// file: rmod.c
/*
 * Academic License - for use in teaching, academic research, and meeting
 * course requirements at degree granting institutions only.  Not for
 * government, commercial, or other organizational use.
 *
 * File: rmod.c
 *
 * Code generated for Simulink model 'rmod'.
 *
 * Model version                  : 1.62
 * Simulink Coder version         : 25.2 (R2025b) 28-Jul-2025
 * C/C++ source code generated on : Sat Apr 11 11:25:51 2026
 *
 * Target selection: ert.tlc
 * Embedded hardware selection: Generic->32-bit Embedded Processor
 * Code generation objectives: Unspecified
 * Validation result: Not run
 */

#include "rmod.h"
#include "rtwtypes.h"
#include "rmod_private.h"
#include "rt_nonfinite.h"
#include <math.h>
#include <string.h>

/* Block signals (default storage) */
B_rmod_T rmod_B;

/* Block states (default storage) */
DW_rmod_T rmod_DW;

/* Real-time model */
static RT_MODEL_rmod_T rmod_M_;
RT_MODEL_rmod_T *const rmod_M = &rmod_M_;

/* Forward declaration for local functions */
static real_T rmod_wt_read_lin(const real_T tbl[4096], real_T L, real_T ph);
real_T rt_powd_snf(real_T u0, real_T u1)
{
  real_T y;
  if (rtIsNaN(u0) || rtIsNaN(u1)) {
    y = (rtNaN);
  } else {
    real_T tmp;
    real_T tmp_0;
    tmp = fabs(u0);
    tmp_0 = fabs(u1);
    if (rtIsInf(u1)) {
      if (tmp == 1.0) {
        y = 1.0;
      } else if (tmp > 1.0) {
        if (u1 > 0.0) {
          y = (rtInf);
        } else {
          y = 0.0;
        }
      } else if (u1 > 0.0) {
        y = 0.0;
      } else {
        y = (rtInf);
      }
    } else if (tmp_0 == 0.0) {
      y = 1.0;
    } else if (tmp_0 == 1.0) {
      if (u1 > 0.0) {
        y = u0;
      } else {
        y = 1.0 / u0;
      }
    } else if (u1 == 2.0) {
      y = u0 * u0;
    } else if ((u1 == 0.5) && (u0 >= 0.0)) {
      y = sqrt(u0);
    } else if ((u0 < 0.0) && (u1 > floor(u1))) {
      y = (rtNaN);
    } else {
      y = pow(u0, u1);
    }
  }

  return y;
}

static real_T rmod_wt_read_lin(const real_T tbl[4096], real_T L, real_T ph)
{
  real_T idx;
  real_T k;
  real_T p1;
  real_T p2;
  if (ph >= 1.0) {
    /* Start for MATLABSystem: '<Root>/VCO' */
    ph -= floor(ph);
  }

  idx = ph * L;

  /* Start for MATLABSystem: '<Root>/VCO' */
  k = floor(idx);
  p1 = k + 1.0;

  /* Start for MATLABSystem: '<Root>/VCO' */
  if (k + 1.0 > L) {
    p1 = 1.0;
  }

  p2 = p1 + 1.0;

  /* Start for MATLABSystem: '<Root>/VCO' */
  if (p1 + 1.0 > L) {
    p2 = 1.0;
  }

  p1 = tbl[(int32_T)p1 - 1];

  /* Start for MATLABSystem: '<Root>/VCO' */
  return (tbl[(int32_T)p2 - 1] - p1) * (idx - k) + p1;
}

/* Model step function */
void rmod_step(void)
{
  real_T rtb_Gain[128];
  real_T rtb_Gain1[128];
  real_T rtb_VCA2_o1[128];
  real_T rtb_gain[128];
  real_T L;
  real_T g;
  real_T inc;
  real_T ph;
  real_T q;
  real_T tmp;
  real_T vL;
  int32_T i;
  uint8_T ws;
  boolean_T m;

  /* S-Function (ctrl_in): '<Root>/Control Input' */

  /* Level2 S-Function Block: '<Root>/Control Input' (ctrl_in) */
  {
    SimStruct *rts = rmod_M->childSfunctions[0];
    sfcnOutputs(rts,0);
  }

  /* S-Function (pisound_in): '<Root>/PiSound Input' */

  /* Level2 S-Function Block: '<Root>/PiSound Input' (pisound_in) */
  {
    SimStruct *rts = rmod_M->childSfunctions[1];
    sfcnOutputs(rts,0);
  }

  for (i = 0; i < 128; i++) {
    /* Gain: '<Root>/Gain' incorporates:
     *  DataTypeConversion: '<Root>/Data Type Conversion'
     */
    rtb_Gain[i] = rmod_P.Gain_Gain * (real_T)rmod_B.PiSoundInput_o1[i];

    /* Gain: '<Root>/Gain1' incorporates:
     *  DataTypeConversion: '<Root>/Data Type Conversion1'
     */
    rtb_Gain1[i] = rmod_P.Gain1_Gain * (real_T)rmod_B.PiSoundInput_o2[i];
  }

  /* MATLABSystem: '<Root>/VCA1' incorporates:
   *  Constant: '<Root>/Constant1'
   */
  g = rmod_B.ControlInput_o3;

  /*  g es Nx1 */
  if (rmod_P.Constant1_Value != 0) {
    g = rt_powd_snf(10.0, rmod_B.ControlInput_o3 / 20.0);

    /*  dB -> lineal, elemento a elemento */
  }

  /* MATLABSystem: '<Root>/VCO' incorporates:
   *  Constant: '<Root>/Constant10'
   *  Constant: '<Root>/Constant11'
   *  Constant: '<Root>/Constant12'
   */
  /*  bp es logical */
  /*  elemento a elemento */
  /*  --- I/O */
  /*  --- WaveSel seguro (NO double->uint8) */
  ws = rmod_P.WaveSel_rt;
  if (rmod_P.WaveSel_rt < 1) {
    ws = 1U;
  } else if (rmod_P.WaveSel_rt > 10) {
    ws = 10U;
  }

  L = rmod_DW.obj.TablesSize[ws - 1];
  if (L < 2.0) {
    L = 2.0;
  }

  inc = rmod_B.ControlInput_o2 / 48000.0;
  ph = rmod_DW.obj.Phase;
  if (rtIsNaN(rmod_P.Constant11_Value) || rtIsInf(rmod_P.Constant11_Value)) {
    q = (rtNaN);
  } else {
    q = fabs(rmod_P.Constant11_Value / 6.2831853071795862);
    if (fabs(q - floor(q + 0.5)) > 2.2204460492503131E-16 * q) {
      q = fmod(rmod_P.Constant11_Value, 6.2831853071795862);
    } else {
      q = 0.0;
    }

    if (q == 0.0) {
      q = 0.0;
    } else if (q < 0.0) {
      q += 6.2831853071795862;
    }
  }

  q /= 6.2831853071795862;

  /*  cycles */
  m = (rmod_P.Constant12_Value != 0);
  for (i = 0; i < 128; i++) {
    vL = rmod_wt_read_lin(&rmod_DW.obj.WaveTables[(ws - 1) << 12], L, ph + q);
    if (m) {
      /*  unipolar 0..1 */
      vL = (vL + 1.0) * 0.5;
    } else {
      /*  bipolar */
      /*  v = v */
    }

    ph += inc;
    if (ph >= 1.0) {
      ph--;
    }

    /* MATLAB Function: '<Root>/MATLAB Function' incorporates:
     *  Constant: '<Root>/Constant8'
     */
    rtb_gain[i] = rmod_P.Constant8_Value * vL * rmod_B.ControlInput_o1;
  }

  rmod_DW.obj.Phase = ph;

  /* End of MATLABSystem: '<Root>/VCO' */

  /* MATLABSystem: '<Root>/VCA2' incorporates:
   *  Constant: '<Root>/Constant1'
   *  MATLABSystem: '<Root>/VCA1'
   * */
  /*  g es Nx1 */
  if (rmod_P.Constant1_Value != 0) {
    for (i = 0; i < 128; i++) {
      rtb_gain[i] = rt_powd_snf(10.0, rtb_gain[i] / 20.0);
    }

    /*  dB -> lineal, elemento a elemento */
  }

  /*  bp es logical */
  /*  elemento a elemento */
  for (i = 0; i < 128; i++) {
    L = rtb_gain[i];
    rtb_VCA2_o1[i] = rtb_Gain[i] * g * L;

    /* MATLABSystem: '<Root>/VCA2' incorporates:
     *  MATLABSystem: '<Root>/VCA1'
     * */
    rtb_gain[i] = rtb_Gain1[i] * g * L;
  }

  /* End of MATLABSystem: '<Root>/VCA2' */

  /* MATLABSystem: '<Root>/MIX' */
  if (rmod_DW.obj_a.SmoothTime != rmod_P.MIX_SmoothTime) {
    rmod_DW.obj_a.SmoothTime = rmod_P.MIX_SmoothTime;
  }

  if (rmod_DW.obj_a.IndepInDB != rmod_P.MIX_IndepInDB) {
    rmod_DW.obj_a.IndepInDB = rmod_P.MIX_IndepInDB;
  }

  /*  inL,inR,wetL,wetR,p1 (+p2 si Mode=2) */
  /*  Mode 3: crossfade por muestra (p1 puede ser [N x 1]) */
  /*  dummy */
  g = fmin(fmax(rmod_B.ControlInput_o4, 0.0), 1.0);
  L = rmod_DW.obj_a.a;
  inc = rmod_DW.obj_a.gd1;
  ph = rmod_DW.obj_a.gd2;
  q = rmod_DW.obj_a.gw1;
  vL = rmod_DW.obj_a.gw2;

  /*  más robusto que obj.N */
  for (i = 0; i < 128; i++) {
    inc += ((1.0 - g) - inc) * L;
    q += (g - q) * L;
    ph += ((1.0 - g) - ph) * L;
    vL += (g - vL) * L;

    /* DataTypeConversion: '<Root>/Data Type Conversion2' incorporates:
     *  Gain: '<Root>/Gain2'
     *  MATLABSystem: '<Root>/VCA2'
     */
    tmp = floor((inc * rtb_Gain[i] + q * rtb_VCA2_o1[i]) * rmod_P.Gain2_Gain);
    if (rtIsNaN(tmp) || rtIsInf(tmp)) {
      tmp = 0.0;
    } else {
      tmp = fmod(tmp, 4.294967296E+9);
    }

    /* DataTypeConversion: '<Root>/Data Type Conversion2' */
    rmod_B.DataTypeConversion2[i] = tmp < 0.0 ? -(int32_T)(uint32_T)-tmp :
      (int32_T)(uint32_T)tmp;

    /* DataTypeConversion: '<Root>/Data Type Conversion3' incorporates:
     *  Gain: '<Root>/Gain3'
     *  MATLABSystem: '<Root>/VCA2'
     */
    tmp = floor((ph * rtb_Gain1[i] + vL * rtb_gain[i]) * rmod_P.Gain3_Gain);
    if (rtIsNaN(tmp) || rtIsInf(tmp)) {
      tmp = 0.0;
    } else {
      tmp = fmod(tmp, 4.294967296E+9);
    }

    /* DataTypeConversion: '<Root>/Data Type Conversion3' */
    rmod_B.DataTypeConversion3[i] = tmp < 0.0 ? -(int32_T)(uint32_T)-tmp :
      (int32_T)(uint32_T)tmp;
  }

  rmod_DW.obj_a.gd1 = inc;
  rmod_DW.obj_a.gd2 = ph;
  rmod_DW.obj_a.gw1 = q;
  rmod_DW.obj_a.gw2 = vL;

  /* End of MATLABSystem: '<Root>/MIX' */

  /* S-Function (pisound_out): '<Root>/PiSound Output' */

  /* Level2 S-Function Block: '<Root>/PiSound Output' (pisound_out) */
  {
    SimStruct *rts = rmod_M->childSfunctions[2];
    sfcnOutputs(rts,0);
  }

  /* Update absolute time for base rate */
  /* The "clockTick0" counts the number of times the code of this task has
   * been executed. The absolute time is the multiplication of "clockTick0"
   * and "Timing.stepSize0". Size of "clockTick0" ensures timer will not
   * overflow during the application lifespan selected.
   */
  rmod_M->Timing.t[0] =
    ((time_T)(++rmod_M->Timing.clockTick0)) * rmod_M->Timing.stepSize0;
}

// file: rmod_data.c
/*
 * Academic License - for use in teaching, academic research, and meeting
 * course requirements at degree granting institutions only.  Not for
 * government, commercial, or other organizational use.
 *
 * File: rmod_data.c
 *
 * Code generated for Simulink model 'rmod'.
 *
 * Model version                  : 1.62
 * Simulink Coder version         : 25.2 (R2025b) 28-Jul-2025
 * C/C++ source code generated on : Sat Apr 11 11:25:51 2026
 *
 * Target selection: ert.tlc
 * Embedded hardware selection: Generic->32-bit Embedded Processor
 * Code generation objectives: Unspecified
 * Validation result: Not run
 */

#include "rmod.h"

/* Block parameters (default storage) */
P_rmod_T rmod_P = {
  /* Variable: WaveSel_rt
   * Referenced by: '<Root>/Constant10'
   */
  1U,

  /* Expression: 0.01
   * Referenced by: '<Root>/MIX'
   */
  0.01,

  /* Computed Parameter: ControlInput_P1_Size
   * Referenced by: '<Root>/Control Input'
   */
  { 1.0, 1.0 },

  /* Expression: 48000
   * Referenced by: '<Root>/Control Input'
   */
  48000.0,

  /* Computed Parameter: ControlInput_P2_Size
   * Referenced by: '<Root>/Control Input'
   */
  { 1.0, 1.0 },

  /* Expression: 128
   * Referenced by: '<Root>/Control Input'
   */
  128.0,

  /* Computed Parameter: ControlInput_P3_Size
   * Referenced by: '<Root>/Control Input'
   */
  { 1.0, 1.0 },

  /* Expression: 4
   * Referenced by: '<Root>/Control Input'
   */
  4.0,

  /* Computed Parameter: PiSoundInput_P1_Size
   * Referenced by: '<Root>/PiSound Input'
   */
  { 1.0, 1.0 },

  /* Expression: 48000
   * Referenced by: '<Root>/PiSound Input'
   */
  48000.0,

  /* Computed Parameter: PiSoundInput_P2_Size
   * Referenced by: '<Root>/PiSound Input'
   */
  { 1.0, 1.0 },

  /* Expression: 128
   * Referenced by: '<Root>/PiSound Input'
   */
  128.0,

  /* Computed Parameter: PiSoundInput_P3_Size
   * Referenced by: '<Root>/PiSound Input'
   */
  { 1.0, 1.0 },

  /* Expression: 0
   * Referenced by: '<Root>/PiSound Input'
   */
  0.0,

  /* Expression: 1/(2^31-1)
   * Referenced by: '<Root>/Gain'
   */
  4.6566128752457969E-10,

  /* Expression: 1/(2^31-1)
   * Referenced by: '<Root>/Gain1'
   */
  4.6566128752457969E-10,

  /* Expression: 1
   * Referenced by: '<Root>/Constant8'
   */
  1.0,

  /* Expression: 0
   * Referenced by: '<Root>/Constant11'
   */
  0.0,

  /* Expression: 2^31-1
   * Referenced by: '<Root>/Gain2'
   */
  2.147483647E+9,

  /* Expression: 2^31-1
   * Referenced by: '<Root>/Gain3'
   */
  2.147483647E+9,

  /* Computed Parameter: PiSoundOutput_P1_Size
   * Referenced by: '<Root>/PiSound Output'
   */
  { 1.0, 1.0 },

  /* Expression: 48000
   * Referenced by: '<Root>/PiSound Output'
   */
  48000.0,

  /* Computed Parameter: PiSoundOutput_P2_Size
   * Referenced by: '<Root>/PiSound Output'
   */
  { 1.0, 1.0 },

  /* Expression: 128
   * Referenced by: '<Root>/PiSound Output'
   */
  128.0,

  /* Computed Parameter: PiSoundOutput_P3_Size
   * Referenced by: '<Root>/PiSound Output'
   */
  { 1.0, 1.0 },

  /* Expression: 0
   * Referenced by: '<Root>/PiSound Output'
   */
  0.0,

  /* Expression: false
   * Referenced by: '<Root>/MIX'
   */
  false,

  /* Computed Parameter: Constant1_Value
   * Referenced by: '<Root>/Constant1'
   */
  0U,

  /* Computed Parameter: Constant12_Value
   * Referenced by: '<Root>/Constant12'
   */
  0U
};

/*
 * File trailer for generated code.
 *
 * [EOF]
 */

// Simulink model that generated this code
simulink model "rmod"  (R2025b)
settings: Solver=FixedStepDiscrete  StartTime=0.0  StopTime=inf  RelTol=1e-3
undefined symbols (not defined in the file): WaveSel_rt

== system rmod ==
  Constant1 : Constant  Value=0  OutDataTypeStr=uint8
  Constant10 : Constant  Value=WaveSel_rt  OutDataTypeStr=uint8
  Constant11 : Constant  Value=0  OutDataTypeStr=double
  Constant12 : Constant  Value=0  OutDataTypeStr=uint8
  Constant8 : Constant  OutDataTypeStr=double
  Control Input : S-Function  FunctionName=ctrl_in  Parameters=48000, 128, 4  SFunctionDeploymentMode=off  EnableBusSupport=off
  Data Type Conversion : DataTypeConversion  OutDataTypeStr=double  SaturateOnIntegerOverflow=off  RndMeth=Floor
  Data Type Conversion1 : DataTypeConversion  OutDataTypeStr=double  SaturateOnIntegerOverflow=off  RndMeth=Floor
  Data Type Conversion2 : DataTypeConversion  OutDataTypeStr=int32  SaturateOnIntegerOverflow=off  RndMeth=Floor
  Data Type Conversion3 : DataTypeConversion  OutDataTypeStr=int32  SaturateOnIntegerOverflow=off  RndMeth=Floor
  Gain : Gain  Gain=1/(2^31-1)  Multiplication=Matrix(K*u)
  Gain1 : Gain  Gain=1/(2^31-1)  Multiplication=Matrix(K*u)
  Gain2 : Gain  Gain=2^31-1  Multiplication=Matrix(K*u)
  Gain3 : Gain  Gain=2^31-1  Multiplication=Matrix(K*u)
  MATLAB Function : MATLAB Function  TreatAsAtomicUnit=on
  MIX : MATLABSystem  System=mix_sys  N=128  Fs=48000  Mode=uint8(0)  SmoothTime=0.01  IndepInDB=false  SimulateUsing=Code generation
  PiSound Input : S-Function  FunctionName=pisound_in  Parameters=48000, 128, 0  SFunctionDeploymentMode=off  EnableBusSupport=off
  PiSound Output : S-Function  FunctionName=pisound_out  Parameters=48000, 128, 0  SFunctionDeploymentMode=off  EnableBusSupport=off
  VCA1 : MATLABSystem  System=vca_sys  N=128  Fs=48000  bypass=uint8(0)  SimulateUsing=Code generation
  VCA2 : MATLABSystem  System=vca_sys  N=128  Fs=48000  bypass=uint8(0)  SimulateUsing=Code generation
  VCO : MATLABSystem  System=vco_sys  N=128  Fs=48000  OutMaxL=4096  InFixL=1024  SimulateUsing=Code generation
  wires:
  PiSound Input/1 -> Data Type Conversion/1
  PiSound Input/2 -> Data Type Conversion1/1
  Data Type Conversion/1 -> Gain/1
  Data Type Conversion1/1 -> Gain1/1
  Gain2/1 -> Data Type Conversion2/1
  Gain3/1 -> Data Type Conversion3/1
  Data Type Conversion2/1 -> PiSound Output/1
  Data Type Conversion3/1 -> PiSound Output/2
  VCA1/2 -> VCA2/2
  Constant1/1 -> VCA1/4, VCA2/4
  Constant8/1 -> VCO/1
  Constant10/1 -> VCO/4
  Constant11/1 -> VCO/3
  Constant12/1 -> VCO/5
  VCO/1 -> MATLAB Function/1(lfo)
  MATLAB Function/1(gain) -> VCA2/3
  Control Input/1 -> MATLAB Function/2(depth)
  Control Input/2 -> VCO/2
  MIX/1 -> Gain2/1
  MIX/2 -> Gain3/1
  VCA1/1 -> VCA2/1
  Control Input/3 -> VCA1/3
  Gain/1 -> MIX/1, VCA1/1
  Gain1/1 -> MIX/2, VCA1/2
  VCA2/1 -> MIX/3
  VCA2/2 -> MIX/4
  Control Input/4 -> MIX/5

== matlab function rmod/MATLAB Function ==
function gain = ring_gain(lfo, depth)
% ring_gain  Convierte la salida del LFO en ganancia bipolar para VCA
%
% Entradas:
%   lfo   : [N x 1] double  salida del LFO en [-1, 1]
%   depth : scalar double   profundidad de modulación [0, 1]
%
% Salida:
%   gain  : [N x 1] double  ganancia bipolar para VCA modo lineal

    gain = depth * lfo;
end
